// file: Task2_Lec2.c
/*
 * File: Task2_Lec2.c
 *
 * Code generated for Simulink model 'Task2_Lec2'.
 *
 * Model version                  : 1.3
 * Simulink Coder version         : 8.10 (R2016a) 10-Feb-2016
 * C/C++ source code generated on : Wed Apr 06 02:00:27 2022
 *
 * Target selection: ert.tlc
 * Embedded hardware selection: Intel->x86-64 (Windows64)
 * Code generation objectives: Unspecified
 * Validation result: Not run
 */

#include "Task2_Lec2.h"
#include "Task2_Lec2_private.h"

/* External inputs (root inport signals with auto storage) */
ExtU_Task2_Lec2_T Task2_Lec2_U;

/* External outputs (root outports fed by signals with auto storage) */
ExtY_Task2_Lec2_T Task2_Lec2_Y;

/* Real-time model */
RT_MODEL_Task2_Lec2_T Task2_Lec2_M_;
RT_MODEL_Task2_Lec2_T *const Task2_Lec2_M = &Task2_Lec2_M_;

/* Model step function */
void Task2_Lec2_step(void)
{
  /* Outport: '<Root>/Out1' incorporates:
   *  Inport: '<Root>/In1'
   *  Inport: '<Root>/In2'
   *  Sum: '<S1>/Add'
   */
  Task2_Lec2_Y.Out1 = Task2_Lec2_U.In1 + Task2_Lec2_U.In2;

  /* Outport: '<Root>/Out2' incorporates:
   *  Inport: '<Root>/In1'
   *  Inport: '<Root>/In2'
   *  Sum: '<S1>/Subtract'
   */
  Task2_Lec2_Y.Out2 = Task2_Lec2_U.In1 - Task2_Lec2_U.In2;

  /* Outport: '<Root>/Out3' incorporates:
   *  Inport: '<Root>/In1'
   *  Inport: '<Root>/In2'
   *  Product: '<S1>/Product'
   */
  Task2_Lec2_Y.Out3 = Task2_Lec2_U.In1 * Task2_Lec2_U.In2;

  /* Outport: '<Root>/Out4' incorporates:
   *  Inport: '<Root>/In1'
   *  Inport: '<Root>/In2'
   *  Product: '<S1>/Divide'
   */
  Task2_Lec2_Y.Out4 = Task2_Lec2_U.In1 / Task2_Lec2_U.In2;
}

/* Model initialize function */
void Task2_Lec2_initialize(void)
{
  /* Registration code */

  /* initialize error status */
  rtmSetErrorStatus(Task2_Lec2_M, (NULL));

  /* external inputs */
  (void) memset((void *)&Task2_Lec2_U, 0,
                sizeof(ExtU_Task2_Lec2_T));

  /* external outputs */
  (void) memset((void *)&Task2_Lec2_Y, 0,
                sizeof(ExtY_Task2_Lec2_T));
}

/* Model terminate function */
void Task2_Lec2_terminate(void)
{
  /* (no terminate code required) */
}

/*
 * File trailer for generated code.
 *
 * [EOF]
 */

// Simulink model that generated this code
simulink model "Task2_Lec2"  (R2016a)
settings: Solver=FixedStepDiscrete  StartTime=0.0  StopTime=10.0  RelTol=1e-3

== system Task2_Lec2 ==
  In1 : Inport
  In2 : Inport  Port=2
  Subsystem : Subsystem
  Out1 : Outport
  Out2 : Outport  Port=2
  Out3 : Outport  Port=3
  Out4 : Outport  Port=4
  wires:
  In1/1 -> Subsystem/1(In1)
  In2/1 -> Subsystem/2(In2)
  Subsystem/1(Out1) -> Out1/1
  Subsystem/2(Out2) -> Out2/1
  Subsystem/3(Out3) -> Out3/1
  Subsystem/4(Out4) -> Out4/1

== system Task2_Lec2/Subsystem ==
  In1 : Inport
  In2 : Inport  Port=2
  Add : Sum
  Divide : Product  Inputs=*/
  Product : Product
  Subtract : Sum  Inputs=+-
  Out1 : Outport
  Out2 : Outport  Port=2
  Out3 : Outport  Port=3
  Out4 : Outport  Port=4
  wires:
  In2/1 -> Divide/2, Product/2, Subtract/2, Add/2
  Add/1 -> Out1/1
  In1/1 -> Divide/1, Product/1, Subtract/1, Add/1
  Divide/1 -> Out4/1
  Subtract/1 -> Out2/1
  Product/1 -> Out3/1
